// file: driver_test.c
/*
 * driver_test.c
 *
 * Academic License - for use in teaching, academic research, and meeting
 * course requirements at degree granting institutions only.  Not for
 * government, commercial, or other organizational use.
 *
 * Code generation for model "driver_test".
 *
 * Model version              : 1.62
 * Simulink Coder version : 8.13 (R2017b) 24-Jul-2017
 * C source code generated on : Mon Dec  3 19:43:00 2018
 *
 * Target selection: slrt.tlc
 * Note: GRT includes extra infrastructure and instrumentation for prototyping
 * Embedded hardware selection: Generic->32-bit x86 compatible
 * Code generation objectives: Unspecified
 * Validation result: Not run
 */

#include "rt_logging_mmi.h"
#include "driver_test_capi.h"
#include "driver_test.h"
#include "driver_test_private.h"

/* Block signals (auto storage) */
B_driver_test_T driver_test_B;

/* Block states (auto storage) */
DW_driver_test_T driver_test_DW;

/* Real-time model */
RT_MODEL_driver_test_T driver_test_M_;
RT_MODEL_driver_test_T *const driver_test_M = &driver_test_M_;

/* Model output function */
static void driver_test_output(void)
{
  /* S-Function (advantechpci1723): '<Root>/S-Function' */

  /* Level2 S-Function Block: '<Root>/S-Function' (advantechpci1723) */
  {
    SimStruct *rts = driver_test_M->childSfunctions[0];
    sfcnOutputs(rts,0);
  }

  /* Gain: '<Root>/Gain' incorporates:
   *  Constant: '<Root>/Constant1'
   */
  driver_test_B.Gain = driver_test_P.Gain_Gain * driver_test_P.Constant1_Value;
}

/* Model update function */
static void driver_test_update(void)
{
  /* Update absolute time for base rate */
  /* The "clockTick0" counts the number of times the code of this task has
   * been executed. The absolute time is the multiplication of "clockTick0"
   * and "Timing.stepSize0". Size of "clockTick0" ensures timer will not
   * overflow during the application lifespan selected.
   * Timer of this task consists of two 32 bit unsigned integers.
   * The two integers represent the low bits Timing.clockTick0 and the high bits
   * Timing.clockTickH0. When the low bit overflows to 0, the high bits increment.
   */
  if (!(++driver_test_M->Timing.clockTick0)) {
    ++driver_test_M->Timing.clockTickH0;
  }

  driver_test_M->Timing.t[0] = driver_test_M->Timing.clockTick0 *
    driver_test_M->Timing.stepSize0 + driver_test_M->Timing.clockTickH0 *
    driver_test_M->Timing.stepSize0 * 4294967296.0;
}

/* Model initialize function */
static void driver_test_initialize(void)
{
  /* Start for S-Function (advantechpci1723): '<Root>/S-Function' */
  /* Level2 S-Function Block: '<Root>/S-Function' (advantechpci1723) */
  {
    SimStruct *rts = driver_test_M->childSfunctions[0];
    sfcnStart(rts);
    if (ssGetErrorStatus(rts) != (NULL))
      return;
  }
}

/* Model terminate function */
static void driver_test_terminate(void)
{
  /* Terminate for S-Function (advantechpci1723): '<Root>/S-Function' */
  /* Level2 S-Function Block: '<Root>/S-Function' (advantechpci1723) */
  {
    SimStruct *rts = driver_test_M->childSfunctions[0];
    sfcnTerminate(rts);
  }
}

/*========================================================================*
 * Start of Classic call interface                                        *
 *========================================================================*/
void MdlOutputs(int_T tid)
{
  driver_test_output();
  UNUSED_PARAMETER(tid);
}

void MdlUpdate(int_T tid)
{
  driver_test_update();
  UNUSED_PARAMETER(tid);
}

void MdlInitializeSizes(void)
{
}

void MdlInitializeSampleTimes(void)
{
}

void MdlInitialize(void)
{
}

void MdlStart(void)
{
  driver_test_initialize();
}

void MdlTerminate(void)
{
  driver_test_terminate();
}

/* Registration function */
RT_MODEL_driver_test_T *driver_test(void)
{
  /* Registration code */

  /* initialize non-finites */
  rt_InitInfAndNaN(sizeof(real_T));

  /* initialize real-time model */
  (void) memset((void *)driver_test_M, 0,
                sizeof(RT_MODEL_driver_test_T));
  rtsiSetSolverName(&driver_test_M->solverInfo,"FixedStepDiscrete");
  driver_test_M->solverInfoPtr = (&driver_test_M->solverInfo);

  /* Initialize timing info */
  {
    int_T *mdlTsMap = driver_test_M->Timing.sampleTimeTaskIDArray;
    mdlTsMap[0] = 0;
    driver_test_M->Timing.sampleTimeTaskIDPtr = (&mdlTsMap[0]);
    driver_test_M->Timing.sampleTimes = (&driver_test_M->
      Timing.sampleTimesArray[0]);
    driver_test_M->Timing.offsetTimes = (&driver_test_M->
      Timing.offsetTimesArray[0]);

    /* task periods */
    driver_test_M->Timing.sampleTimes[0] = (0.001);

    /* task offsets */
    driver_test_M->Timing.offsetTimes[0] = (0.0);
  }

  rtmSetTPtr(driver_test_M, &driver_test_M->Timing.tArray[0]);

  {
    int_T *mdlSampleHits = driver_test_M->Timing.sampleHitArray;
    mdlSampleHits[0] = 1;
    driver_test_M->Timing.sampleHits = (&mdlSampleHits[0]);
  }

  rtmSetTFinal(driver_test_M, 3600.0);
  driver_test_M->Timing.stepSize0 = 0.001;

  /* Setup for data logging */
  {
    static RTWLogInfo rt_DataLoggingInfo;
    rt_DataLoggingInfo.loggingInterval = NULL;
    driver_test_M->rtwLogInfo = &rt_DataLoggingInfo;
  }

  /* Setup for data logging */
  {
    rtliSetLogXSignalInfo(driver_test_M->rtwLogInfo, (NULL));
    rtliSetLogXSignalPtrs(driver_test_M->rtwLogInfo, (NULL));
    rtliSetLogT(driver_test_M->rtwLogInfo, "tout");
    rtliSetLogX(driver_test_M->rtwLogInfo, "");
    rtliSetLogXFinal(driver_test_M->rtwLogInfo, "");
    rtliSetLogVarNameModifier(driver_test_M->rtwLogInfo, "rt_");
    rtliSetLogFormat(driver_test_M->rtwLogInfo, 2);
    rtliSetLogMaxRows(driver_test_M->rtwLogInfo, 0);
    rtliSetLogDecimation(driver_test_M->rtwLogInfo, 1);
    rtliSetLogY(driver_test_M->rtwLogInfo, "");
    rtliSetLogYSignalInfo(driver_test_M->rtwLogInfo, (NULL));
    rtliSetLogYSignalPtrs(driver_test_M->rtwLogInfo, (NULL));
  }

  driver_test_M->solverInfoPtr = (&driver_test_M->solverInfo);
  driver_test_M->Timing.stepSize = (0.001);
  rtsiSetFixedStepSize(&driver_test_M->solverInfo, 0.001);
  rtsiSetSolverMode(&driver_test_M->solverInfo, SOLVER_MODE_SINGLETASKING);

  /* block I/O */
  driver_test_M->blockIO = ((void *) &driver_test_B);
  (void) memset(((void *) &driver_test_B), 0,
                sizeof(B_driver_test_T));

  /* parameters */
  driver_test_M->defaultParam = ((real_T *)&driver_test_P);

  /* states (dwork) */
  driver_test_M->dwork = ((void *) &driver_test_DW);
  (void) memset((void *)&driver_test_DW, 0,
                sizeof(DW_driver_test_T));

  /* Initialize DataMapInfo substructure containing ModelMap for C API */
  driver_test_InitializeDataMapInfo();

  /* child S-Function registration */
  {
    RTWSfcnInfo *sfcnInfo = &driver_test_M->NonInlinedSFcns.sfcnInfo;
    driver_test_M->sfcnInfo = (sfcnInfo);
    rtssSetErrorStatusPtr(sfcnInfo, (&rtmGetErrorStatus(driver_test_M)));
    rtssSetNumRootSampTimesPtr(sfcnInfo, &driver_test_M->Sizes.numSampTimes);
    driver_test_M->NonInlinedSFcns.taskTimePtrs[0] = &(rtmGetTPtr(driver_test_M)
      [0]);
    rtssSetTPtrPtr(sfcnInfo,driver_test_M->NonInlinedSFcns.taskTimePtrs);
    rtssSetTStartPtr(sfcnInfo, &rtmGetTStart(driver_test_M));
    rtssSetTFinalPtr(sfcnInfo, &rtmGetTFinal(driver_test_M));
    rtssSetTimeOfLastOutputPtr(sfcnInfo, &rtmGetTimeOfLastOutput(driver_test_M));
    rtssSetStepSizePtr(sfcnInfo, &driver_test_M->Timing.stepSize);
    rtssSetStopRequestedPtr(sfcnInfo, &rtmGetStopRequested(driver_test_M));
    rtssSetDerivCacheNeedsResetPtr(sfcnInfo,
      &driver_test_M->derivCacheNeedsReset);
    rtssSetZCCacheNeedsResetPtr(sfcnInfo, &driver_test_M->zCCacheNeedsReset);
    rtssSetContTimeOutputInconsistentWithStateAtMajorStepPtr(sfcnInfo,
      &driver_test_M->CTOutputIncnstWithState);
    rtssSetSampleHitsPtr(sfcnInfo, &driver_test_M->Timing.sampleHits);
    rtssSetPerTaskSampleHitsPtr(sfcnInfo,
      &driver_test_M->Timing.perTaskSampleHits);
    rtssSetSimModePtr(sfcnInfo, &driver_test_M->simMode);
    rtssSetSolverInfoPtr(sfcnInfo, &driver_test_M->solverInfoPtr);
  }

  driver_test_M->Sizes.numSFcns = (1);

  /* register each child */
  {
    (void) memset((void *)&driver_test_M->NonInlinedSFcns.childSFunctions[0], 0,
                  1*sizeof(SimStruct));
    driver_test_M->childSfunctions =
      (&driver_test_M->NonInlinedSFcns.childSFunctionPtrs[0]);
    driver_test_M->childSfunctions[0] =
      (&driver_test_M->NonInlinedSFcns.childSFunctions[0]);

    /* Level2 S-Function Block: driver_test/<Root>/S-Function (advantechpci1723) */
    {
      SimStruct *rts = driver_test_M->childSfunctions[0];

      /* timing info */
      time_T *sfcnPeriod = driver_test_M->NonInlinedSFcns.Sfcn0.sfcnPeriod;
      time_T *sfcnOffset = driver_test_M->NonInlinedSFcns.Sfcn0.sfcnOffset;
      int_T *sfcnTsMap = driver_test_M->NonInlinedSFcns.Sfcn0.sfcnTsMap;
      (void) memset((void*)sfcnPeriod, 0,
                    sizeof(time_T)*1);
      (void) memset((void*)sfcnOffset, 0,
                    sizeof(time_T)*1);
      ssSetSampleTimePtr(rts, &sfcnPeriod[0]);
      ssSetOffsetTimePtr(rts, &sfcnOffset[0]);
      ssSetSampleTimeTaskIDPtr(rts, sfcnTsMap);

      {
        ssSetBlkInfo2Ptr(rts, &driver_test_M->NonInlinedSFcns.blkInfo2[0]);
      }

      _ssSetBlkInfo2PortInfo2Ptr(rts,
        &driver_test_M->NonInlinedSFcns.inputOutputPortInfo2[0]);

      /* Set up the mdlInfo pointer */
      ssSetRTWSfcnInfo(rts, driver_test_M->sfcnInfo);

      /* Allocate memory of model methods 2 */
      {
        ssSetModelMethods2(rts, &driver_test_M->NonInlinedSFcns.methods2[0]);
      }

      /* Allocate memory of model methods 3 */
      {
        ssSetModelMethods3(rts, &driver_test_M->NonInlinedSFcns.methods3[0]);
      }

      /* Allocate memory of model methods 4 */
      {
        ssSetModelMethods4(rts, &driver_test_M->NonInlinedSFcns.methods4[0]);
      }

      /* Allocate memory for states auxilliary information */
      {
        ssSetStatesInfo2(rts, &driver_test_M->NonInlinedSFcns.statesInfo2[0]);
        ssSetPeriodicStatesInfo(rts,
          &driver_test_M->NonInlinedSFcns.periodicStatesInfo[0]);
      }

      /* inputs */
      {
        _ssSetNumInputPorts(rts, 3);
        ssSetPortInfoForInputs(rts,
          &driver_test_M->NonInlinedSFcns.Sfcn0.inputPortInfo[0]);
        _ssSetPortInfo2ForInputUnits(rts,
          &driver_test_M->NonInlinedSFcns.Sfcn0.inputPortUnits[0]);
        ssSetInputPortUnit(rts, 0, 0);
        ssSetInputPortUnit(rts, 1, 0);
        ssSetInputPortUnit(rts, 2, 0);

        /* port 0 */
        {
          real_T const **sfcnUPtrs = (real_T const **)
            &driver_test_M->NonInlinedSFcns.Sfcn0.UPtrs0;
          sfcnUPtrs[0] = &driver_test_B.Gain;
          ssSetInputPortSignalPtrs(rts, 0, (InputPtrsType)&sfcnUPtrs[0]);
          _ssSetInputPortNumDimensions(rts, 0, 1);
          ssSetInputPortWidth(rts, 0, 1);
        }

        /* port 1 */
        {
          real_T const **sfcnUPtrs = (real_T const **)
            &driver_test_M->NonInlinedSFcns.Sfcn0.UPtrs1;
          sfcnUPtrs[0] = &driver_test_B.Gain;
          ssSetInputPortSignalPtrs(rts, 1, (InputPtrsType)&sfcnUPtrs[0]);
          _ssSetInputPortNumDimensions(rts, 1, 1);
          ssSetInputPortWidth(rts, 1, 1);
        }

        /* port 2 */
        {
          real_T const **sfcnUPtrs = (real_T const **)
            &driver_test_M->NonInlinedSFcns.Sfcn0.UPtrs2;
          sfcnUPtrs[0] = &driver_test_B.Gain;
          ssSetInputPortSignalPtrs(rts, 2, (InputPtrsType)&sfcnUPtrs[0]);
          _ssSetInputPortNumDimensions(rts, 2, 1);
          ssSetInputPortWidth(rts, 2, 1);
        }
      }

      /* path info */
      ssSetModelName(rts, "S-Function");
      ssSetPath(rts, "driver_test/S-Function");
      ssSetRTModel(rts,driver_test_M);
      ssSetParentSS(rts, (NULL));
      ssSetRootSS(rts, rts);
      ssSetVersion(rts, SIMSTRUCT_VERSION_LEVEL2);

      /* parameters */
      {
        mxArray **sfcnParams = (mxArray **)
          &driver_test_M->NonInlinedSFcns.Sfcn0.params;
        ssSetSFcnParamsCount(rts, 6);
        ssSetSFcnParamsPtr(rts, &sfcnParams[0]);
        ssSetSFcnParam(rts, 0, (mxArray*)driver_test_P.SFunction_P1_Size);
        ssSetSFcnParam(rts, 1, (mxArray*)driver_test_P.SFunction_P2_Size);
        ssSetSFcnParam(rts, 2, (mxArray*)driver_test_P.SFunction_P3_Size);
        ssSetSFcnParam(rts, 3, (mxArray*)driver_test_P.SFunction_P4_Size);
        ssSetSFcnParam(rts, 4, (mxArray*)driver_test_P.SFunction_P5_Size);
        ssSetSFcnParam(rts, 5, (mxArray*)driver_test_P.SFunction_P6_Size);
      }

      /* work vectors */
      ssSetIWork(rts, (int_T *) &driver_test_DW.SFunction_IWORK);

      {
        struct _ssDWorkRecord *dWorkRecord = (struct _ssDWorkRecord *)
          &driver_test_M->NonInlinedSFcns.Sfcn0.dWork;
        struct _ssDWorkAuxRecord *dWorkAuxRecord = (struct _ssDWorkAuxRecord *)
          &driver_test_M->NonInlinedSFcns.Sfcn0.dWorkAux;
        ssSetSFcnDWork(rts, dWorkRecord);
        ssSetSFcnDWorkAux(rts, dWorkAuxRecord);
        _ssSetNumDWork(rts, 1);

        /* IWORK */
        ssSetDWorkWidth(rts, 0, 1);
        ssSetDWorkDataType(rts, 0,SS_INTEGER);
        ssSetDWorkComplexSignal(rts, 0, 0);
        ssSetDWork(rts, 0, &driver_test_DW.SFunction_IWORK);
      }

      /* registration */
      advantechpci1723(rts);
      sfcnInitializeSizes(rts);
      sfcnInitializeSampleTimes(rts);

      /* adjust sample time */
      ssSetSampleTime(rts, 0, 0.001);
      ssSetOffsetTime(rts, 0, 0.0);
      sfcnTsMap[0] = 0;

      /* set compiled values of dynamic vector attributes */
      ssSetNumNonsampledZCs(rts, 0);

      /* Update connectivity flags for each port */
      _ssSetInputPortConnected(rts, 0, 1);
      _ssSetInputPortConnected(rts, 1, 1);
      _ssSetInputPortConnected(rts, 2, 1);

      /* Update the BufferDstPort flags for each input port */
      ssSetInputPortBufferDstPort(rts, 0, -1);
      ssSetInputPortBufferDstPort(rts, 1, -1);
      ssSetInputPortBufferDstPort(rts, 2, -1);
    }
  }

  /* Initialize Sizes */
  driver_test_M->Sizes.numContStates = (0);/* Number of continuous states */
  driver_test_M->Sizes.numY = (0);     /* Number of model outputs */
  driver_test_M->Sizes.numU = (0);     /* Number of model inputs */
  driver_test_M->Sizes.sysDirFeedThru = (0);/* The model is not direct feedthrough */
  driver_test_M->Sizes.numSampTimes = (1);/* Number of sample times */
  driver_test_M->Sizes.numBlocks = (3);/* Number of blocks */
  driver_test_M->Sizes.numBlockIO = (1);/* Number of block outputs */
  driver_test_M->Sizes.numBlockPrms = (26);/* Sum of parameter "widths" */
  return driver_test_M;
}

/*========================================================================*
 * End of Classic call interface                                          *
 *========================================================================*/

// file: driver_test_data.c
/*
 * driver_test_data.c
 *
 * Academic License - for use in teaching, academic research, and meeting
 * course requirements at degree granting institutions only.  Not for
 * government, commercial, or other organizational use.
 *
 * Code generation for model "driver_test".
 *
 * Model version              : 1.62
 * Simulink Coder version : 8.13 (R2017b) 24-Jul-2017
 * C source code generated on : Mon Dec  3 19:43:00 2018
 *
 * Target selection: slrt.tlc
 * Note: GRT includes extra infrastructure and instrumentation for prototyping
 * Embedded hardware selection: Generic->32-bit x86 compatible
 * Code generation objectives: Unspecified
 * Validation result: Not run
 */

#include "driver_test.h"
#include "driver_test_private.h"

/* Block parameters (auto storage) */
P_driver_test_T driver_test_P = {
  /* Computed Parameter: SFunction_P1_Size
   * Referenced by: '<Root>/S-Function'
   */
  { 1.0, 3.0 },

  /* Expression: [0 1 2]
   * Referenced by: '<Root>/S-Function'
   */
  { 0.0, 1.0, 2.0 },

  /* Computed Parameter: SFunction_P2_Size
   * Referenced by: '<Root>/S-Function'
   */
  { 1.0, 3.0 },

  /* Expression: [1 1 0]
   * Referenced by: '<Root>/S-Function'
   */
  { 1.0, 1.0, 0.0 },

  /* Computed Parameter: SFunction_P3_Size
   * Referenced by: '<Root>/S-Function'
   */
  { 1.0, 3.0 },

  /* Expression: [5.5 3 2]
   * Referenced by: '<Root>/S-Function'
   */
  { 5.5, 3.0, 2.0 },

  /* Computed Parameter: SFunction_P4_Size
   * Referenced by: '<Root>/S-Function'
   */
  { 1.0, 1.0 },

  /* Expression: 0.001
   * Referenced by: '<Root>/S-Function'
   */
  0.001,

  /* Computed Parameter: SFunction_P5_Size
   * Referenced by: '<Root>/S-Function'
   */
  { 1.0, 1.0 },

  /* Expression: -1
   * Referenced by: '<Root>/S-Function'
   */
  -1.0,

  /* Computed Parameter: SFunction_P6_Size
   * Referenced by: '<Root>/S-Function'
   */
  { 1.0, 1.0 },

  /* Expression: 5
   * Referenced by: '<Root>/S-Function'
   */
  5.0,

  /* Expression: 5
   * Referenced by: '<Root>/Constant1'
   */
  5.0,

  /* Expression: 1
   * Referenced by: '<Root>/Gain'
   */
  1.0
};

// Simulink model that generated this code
simulink model "driver_test"  (R2017b)
settings: Solver=FixedStepDiscrete  StartTime=0.0  StopTime=3600  FixedStep=0.001  RelTol=1e-3  EnableMultiTasking=on

== system driver_test ==
  Constant1 : Constant  Value=5
  Gain : Gain
  S-Function : S-Function  FunctionName=advantechpci1723  Parameters=[0 1 2],[1 1 0],[5.5 3 2],0.001,-1,5  SFunctionDeploymentMode=off  EnableBusSupport=off
  wires:
  Constant1/1 -> Gain/1
  Gain/1 -> S-Function/3, S-Function/2, S-Function/1
